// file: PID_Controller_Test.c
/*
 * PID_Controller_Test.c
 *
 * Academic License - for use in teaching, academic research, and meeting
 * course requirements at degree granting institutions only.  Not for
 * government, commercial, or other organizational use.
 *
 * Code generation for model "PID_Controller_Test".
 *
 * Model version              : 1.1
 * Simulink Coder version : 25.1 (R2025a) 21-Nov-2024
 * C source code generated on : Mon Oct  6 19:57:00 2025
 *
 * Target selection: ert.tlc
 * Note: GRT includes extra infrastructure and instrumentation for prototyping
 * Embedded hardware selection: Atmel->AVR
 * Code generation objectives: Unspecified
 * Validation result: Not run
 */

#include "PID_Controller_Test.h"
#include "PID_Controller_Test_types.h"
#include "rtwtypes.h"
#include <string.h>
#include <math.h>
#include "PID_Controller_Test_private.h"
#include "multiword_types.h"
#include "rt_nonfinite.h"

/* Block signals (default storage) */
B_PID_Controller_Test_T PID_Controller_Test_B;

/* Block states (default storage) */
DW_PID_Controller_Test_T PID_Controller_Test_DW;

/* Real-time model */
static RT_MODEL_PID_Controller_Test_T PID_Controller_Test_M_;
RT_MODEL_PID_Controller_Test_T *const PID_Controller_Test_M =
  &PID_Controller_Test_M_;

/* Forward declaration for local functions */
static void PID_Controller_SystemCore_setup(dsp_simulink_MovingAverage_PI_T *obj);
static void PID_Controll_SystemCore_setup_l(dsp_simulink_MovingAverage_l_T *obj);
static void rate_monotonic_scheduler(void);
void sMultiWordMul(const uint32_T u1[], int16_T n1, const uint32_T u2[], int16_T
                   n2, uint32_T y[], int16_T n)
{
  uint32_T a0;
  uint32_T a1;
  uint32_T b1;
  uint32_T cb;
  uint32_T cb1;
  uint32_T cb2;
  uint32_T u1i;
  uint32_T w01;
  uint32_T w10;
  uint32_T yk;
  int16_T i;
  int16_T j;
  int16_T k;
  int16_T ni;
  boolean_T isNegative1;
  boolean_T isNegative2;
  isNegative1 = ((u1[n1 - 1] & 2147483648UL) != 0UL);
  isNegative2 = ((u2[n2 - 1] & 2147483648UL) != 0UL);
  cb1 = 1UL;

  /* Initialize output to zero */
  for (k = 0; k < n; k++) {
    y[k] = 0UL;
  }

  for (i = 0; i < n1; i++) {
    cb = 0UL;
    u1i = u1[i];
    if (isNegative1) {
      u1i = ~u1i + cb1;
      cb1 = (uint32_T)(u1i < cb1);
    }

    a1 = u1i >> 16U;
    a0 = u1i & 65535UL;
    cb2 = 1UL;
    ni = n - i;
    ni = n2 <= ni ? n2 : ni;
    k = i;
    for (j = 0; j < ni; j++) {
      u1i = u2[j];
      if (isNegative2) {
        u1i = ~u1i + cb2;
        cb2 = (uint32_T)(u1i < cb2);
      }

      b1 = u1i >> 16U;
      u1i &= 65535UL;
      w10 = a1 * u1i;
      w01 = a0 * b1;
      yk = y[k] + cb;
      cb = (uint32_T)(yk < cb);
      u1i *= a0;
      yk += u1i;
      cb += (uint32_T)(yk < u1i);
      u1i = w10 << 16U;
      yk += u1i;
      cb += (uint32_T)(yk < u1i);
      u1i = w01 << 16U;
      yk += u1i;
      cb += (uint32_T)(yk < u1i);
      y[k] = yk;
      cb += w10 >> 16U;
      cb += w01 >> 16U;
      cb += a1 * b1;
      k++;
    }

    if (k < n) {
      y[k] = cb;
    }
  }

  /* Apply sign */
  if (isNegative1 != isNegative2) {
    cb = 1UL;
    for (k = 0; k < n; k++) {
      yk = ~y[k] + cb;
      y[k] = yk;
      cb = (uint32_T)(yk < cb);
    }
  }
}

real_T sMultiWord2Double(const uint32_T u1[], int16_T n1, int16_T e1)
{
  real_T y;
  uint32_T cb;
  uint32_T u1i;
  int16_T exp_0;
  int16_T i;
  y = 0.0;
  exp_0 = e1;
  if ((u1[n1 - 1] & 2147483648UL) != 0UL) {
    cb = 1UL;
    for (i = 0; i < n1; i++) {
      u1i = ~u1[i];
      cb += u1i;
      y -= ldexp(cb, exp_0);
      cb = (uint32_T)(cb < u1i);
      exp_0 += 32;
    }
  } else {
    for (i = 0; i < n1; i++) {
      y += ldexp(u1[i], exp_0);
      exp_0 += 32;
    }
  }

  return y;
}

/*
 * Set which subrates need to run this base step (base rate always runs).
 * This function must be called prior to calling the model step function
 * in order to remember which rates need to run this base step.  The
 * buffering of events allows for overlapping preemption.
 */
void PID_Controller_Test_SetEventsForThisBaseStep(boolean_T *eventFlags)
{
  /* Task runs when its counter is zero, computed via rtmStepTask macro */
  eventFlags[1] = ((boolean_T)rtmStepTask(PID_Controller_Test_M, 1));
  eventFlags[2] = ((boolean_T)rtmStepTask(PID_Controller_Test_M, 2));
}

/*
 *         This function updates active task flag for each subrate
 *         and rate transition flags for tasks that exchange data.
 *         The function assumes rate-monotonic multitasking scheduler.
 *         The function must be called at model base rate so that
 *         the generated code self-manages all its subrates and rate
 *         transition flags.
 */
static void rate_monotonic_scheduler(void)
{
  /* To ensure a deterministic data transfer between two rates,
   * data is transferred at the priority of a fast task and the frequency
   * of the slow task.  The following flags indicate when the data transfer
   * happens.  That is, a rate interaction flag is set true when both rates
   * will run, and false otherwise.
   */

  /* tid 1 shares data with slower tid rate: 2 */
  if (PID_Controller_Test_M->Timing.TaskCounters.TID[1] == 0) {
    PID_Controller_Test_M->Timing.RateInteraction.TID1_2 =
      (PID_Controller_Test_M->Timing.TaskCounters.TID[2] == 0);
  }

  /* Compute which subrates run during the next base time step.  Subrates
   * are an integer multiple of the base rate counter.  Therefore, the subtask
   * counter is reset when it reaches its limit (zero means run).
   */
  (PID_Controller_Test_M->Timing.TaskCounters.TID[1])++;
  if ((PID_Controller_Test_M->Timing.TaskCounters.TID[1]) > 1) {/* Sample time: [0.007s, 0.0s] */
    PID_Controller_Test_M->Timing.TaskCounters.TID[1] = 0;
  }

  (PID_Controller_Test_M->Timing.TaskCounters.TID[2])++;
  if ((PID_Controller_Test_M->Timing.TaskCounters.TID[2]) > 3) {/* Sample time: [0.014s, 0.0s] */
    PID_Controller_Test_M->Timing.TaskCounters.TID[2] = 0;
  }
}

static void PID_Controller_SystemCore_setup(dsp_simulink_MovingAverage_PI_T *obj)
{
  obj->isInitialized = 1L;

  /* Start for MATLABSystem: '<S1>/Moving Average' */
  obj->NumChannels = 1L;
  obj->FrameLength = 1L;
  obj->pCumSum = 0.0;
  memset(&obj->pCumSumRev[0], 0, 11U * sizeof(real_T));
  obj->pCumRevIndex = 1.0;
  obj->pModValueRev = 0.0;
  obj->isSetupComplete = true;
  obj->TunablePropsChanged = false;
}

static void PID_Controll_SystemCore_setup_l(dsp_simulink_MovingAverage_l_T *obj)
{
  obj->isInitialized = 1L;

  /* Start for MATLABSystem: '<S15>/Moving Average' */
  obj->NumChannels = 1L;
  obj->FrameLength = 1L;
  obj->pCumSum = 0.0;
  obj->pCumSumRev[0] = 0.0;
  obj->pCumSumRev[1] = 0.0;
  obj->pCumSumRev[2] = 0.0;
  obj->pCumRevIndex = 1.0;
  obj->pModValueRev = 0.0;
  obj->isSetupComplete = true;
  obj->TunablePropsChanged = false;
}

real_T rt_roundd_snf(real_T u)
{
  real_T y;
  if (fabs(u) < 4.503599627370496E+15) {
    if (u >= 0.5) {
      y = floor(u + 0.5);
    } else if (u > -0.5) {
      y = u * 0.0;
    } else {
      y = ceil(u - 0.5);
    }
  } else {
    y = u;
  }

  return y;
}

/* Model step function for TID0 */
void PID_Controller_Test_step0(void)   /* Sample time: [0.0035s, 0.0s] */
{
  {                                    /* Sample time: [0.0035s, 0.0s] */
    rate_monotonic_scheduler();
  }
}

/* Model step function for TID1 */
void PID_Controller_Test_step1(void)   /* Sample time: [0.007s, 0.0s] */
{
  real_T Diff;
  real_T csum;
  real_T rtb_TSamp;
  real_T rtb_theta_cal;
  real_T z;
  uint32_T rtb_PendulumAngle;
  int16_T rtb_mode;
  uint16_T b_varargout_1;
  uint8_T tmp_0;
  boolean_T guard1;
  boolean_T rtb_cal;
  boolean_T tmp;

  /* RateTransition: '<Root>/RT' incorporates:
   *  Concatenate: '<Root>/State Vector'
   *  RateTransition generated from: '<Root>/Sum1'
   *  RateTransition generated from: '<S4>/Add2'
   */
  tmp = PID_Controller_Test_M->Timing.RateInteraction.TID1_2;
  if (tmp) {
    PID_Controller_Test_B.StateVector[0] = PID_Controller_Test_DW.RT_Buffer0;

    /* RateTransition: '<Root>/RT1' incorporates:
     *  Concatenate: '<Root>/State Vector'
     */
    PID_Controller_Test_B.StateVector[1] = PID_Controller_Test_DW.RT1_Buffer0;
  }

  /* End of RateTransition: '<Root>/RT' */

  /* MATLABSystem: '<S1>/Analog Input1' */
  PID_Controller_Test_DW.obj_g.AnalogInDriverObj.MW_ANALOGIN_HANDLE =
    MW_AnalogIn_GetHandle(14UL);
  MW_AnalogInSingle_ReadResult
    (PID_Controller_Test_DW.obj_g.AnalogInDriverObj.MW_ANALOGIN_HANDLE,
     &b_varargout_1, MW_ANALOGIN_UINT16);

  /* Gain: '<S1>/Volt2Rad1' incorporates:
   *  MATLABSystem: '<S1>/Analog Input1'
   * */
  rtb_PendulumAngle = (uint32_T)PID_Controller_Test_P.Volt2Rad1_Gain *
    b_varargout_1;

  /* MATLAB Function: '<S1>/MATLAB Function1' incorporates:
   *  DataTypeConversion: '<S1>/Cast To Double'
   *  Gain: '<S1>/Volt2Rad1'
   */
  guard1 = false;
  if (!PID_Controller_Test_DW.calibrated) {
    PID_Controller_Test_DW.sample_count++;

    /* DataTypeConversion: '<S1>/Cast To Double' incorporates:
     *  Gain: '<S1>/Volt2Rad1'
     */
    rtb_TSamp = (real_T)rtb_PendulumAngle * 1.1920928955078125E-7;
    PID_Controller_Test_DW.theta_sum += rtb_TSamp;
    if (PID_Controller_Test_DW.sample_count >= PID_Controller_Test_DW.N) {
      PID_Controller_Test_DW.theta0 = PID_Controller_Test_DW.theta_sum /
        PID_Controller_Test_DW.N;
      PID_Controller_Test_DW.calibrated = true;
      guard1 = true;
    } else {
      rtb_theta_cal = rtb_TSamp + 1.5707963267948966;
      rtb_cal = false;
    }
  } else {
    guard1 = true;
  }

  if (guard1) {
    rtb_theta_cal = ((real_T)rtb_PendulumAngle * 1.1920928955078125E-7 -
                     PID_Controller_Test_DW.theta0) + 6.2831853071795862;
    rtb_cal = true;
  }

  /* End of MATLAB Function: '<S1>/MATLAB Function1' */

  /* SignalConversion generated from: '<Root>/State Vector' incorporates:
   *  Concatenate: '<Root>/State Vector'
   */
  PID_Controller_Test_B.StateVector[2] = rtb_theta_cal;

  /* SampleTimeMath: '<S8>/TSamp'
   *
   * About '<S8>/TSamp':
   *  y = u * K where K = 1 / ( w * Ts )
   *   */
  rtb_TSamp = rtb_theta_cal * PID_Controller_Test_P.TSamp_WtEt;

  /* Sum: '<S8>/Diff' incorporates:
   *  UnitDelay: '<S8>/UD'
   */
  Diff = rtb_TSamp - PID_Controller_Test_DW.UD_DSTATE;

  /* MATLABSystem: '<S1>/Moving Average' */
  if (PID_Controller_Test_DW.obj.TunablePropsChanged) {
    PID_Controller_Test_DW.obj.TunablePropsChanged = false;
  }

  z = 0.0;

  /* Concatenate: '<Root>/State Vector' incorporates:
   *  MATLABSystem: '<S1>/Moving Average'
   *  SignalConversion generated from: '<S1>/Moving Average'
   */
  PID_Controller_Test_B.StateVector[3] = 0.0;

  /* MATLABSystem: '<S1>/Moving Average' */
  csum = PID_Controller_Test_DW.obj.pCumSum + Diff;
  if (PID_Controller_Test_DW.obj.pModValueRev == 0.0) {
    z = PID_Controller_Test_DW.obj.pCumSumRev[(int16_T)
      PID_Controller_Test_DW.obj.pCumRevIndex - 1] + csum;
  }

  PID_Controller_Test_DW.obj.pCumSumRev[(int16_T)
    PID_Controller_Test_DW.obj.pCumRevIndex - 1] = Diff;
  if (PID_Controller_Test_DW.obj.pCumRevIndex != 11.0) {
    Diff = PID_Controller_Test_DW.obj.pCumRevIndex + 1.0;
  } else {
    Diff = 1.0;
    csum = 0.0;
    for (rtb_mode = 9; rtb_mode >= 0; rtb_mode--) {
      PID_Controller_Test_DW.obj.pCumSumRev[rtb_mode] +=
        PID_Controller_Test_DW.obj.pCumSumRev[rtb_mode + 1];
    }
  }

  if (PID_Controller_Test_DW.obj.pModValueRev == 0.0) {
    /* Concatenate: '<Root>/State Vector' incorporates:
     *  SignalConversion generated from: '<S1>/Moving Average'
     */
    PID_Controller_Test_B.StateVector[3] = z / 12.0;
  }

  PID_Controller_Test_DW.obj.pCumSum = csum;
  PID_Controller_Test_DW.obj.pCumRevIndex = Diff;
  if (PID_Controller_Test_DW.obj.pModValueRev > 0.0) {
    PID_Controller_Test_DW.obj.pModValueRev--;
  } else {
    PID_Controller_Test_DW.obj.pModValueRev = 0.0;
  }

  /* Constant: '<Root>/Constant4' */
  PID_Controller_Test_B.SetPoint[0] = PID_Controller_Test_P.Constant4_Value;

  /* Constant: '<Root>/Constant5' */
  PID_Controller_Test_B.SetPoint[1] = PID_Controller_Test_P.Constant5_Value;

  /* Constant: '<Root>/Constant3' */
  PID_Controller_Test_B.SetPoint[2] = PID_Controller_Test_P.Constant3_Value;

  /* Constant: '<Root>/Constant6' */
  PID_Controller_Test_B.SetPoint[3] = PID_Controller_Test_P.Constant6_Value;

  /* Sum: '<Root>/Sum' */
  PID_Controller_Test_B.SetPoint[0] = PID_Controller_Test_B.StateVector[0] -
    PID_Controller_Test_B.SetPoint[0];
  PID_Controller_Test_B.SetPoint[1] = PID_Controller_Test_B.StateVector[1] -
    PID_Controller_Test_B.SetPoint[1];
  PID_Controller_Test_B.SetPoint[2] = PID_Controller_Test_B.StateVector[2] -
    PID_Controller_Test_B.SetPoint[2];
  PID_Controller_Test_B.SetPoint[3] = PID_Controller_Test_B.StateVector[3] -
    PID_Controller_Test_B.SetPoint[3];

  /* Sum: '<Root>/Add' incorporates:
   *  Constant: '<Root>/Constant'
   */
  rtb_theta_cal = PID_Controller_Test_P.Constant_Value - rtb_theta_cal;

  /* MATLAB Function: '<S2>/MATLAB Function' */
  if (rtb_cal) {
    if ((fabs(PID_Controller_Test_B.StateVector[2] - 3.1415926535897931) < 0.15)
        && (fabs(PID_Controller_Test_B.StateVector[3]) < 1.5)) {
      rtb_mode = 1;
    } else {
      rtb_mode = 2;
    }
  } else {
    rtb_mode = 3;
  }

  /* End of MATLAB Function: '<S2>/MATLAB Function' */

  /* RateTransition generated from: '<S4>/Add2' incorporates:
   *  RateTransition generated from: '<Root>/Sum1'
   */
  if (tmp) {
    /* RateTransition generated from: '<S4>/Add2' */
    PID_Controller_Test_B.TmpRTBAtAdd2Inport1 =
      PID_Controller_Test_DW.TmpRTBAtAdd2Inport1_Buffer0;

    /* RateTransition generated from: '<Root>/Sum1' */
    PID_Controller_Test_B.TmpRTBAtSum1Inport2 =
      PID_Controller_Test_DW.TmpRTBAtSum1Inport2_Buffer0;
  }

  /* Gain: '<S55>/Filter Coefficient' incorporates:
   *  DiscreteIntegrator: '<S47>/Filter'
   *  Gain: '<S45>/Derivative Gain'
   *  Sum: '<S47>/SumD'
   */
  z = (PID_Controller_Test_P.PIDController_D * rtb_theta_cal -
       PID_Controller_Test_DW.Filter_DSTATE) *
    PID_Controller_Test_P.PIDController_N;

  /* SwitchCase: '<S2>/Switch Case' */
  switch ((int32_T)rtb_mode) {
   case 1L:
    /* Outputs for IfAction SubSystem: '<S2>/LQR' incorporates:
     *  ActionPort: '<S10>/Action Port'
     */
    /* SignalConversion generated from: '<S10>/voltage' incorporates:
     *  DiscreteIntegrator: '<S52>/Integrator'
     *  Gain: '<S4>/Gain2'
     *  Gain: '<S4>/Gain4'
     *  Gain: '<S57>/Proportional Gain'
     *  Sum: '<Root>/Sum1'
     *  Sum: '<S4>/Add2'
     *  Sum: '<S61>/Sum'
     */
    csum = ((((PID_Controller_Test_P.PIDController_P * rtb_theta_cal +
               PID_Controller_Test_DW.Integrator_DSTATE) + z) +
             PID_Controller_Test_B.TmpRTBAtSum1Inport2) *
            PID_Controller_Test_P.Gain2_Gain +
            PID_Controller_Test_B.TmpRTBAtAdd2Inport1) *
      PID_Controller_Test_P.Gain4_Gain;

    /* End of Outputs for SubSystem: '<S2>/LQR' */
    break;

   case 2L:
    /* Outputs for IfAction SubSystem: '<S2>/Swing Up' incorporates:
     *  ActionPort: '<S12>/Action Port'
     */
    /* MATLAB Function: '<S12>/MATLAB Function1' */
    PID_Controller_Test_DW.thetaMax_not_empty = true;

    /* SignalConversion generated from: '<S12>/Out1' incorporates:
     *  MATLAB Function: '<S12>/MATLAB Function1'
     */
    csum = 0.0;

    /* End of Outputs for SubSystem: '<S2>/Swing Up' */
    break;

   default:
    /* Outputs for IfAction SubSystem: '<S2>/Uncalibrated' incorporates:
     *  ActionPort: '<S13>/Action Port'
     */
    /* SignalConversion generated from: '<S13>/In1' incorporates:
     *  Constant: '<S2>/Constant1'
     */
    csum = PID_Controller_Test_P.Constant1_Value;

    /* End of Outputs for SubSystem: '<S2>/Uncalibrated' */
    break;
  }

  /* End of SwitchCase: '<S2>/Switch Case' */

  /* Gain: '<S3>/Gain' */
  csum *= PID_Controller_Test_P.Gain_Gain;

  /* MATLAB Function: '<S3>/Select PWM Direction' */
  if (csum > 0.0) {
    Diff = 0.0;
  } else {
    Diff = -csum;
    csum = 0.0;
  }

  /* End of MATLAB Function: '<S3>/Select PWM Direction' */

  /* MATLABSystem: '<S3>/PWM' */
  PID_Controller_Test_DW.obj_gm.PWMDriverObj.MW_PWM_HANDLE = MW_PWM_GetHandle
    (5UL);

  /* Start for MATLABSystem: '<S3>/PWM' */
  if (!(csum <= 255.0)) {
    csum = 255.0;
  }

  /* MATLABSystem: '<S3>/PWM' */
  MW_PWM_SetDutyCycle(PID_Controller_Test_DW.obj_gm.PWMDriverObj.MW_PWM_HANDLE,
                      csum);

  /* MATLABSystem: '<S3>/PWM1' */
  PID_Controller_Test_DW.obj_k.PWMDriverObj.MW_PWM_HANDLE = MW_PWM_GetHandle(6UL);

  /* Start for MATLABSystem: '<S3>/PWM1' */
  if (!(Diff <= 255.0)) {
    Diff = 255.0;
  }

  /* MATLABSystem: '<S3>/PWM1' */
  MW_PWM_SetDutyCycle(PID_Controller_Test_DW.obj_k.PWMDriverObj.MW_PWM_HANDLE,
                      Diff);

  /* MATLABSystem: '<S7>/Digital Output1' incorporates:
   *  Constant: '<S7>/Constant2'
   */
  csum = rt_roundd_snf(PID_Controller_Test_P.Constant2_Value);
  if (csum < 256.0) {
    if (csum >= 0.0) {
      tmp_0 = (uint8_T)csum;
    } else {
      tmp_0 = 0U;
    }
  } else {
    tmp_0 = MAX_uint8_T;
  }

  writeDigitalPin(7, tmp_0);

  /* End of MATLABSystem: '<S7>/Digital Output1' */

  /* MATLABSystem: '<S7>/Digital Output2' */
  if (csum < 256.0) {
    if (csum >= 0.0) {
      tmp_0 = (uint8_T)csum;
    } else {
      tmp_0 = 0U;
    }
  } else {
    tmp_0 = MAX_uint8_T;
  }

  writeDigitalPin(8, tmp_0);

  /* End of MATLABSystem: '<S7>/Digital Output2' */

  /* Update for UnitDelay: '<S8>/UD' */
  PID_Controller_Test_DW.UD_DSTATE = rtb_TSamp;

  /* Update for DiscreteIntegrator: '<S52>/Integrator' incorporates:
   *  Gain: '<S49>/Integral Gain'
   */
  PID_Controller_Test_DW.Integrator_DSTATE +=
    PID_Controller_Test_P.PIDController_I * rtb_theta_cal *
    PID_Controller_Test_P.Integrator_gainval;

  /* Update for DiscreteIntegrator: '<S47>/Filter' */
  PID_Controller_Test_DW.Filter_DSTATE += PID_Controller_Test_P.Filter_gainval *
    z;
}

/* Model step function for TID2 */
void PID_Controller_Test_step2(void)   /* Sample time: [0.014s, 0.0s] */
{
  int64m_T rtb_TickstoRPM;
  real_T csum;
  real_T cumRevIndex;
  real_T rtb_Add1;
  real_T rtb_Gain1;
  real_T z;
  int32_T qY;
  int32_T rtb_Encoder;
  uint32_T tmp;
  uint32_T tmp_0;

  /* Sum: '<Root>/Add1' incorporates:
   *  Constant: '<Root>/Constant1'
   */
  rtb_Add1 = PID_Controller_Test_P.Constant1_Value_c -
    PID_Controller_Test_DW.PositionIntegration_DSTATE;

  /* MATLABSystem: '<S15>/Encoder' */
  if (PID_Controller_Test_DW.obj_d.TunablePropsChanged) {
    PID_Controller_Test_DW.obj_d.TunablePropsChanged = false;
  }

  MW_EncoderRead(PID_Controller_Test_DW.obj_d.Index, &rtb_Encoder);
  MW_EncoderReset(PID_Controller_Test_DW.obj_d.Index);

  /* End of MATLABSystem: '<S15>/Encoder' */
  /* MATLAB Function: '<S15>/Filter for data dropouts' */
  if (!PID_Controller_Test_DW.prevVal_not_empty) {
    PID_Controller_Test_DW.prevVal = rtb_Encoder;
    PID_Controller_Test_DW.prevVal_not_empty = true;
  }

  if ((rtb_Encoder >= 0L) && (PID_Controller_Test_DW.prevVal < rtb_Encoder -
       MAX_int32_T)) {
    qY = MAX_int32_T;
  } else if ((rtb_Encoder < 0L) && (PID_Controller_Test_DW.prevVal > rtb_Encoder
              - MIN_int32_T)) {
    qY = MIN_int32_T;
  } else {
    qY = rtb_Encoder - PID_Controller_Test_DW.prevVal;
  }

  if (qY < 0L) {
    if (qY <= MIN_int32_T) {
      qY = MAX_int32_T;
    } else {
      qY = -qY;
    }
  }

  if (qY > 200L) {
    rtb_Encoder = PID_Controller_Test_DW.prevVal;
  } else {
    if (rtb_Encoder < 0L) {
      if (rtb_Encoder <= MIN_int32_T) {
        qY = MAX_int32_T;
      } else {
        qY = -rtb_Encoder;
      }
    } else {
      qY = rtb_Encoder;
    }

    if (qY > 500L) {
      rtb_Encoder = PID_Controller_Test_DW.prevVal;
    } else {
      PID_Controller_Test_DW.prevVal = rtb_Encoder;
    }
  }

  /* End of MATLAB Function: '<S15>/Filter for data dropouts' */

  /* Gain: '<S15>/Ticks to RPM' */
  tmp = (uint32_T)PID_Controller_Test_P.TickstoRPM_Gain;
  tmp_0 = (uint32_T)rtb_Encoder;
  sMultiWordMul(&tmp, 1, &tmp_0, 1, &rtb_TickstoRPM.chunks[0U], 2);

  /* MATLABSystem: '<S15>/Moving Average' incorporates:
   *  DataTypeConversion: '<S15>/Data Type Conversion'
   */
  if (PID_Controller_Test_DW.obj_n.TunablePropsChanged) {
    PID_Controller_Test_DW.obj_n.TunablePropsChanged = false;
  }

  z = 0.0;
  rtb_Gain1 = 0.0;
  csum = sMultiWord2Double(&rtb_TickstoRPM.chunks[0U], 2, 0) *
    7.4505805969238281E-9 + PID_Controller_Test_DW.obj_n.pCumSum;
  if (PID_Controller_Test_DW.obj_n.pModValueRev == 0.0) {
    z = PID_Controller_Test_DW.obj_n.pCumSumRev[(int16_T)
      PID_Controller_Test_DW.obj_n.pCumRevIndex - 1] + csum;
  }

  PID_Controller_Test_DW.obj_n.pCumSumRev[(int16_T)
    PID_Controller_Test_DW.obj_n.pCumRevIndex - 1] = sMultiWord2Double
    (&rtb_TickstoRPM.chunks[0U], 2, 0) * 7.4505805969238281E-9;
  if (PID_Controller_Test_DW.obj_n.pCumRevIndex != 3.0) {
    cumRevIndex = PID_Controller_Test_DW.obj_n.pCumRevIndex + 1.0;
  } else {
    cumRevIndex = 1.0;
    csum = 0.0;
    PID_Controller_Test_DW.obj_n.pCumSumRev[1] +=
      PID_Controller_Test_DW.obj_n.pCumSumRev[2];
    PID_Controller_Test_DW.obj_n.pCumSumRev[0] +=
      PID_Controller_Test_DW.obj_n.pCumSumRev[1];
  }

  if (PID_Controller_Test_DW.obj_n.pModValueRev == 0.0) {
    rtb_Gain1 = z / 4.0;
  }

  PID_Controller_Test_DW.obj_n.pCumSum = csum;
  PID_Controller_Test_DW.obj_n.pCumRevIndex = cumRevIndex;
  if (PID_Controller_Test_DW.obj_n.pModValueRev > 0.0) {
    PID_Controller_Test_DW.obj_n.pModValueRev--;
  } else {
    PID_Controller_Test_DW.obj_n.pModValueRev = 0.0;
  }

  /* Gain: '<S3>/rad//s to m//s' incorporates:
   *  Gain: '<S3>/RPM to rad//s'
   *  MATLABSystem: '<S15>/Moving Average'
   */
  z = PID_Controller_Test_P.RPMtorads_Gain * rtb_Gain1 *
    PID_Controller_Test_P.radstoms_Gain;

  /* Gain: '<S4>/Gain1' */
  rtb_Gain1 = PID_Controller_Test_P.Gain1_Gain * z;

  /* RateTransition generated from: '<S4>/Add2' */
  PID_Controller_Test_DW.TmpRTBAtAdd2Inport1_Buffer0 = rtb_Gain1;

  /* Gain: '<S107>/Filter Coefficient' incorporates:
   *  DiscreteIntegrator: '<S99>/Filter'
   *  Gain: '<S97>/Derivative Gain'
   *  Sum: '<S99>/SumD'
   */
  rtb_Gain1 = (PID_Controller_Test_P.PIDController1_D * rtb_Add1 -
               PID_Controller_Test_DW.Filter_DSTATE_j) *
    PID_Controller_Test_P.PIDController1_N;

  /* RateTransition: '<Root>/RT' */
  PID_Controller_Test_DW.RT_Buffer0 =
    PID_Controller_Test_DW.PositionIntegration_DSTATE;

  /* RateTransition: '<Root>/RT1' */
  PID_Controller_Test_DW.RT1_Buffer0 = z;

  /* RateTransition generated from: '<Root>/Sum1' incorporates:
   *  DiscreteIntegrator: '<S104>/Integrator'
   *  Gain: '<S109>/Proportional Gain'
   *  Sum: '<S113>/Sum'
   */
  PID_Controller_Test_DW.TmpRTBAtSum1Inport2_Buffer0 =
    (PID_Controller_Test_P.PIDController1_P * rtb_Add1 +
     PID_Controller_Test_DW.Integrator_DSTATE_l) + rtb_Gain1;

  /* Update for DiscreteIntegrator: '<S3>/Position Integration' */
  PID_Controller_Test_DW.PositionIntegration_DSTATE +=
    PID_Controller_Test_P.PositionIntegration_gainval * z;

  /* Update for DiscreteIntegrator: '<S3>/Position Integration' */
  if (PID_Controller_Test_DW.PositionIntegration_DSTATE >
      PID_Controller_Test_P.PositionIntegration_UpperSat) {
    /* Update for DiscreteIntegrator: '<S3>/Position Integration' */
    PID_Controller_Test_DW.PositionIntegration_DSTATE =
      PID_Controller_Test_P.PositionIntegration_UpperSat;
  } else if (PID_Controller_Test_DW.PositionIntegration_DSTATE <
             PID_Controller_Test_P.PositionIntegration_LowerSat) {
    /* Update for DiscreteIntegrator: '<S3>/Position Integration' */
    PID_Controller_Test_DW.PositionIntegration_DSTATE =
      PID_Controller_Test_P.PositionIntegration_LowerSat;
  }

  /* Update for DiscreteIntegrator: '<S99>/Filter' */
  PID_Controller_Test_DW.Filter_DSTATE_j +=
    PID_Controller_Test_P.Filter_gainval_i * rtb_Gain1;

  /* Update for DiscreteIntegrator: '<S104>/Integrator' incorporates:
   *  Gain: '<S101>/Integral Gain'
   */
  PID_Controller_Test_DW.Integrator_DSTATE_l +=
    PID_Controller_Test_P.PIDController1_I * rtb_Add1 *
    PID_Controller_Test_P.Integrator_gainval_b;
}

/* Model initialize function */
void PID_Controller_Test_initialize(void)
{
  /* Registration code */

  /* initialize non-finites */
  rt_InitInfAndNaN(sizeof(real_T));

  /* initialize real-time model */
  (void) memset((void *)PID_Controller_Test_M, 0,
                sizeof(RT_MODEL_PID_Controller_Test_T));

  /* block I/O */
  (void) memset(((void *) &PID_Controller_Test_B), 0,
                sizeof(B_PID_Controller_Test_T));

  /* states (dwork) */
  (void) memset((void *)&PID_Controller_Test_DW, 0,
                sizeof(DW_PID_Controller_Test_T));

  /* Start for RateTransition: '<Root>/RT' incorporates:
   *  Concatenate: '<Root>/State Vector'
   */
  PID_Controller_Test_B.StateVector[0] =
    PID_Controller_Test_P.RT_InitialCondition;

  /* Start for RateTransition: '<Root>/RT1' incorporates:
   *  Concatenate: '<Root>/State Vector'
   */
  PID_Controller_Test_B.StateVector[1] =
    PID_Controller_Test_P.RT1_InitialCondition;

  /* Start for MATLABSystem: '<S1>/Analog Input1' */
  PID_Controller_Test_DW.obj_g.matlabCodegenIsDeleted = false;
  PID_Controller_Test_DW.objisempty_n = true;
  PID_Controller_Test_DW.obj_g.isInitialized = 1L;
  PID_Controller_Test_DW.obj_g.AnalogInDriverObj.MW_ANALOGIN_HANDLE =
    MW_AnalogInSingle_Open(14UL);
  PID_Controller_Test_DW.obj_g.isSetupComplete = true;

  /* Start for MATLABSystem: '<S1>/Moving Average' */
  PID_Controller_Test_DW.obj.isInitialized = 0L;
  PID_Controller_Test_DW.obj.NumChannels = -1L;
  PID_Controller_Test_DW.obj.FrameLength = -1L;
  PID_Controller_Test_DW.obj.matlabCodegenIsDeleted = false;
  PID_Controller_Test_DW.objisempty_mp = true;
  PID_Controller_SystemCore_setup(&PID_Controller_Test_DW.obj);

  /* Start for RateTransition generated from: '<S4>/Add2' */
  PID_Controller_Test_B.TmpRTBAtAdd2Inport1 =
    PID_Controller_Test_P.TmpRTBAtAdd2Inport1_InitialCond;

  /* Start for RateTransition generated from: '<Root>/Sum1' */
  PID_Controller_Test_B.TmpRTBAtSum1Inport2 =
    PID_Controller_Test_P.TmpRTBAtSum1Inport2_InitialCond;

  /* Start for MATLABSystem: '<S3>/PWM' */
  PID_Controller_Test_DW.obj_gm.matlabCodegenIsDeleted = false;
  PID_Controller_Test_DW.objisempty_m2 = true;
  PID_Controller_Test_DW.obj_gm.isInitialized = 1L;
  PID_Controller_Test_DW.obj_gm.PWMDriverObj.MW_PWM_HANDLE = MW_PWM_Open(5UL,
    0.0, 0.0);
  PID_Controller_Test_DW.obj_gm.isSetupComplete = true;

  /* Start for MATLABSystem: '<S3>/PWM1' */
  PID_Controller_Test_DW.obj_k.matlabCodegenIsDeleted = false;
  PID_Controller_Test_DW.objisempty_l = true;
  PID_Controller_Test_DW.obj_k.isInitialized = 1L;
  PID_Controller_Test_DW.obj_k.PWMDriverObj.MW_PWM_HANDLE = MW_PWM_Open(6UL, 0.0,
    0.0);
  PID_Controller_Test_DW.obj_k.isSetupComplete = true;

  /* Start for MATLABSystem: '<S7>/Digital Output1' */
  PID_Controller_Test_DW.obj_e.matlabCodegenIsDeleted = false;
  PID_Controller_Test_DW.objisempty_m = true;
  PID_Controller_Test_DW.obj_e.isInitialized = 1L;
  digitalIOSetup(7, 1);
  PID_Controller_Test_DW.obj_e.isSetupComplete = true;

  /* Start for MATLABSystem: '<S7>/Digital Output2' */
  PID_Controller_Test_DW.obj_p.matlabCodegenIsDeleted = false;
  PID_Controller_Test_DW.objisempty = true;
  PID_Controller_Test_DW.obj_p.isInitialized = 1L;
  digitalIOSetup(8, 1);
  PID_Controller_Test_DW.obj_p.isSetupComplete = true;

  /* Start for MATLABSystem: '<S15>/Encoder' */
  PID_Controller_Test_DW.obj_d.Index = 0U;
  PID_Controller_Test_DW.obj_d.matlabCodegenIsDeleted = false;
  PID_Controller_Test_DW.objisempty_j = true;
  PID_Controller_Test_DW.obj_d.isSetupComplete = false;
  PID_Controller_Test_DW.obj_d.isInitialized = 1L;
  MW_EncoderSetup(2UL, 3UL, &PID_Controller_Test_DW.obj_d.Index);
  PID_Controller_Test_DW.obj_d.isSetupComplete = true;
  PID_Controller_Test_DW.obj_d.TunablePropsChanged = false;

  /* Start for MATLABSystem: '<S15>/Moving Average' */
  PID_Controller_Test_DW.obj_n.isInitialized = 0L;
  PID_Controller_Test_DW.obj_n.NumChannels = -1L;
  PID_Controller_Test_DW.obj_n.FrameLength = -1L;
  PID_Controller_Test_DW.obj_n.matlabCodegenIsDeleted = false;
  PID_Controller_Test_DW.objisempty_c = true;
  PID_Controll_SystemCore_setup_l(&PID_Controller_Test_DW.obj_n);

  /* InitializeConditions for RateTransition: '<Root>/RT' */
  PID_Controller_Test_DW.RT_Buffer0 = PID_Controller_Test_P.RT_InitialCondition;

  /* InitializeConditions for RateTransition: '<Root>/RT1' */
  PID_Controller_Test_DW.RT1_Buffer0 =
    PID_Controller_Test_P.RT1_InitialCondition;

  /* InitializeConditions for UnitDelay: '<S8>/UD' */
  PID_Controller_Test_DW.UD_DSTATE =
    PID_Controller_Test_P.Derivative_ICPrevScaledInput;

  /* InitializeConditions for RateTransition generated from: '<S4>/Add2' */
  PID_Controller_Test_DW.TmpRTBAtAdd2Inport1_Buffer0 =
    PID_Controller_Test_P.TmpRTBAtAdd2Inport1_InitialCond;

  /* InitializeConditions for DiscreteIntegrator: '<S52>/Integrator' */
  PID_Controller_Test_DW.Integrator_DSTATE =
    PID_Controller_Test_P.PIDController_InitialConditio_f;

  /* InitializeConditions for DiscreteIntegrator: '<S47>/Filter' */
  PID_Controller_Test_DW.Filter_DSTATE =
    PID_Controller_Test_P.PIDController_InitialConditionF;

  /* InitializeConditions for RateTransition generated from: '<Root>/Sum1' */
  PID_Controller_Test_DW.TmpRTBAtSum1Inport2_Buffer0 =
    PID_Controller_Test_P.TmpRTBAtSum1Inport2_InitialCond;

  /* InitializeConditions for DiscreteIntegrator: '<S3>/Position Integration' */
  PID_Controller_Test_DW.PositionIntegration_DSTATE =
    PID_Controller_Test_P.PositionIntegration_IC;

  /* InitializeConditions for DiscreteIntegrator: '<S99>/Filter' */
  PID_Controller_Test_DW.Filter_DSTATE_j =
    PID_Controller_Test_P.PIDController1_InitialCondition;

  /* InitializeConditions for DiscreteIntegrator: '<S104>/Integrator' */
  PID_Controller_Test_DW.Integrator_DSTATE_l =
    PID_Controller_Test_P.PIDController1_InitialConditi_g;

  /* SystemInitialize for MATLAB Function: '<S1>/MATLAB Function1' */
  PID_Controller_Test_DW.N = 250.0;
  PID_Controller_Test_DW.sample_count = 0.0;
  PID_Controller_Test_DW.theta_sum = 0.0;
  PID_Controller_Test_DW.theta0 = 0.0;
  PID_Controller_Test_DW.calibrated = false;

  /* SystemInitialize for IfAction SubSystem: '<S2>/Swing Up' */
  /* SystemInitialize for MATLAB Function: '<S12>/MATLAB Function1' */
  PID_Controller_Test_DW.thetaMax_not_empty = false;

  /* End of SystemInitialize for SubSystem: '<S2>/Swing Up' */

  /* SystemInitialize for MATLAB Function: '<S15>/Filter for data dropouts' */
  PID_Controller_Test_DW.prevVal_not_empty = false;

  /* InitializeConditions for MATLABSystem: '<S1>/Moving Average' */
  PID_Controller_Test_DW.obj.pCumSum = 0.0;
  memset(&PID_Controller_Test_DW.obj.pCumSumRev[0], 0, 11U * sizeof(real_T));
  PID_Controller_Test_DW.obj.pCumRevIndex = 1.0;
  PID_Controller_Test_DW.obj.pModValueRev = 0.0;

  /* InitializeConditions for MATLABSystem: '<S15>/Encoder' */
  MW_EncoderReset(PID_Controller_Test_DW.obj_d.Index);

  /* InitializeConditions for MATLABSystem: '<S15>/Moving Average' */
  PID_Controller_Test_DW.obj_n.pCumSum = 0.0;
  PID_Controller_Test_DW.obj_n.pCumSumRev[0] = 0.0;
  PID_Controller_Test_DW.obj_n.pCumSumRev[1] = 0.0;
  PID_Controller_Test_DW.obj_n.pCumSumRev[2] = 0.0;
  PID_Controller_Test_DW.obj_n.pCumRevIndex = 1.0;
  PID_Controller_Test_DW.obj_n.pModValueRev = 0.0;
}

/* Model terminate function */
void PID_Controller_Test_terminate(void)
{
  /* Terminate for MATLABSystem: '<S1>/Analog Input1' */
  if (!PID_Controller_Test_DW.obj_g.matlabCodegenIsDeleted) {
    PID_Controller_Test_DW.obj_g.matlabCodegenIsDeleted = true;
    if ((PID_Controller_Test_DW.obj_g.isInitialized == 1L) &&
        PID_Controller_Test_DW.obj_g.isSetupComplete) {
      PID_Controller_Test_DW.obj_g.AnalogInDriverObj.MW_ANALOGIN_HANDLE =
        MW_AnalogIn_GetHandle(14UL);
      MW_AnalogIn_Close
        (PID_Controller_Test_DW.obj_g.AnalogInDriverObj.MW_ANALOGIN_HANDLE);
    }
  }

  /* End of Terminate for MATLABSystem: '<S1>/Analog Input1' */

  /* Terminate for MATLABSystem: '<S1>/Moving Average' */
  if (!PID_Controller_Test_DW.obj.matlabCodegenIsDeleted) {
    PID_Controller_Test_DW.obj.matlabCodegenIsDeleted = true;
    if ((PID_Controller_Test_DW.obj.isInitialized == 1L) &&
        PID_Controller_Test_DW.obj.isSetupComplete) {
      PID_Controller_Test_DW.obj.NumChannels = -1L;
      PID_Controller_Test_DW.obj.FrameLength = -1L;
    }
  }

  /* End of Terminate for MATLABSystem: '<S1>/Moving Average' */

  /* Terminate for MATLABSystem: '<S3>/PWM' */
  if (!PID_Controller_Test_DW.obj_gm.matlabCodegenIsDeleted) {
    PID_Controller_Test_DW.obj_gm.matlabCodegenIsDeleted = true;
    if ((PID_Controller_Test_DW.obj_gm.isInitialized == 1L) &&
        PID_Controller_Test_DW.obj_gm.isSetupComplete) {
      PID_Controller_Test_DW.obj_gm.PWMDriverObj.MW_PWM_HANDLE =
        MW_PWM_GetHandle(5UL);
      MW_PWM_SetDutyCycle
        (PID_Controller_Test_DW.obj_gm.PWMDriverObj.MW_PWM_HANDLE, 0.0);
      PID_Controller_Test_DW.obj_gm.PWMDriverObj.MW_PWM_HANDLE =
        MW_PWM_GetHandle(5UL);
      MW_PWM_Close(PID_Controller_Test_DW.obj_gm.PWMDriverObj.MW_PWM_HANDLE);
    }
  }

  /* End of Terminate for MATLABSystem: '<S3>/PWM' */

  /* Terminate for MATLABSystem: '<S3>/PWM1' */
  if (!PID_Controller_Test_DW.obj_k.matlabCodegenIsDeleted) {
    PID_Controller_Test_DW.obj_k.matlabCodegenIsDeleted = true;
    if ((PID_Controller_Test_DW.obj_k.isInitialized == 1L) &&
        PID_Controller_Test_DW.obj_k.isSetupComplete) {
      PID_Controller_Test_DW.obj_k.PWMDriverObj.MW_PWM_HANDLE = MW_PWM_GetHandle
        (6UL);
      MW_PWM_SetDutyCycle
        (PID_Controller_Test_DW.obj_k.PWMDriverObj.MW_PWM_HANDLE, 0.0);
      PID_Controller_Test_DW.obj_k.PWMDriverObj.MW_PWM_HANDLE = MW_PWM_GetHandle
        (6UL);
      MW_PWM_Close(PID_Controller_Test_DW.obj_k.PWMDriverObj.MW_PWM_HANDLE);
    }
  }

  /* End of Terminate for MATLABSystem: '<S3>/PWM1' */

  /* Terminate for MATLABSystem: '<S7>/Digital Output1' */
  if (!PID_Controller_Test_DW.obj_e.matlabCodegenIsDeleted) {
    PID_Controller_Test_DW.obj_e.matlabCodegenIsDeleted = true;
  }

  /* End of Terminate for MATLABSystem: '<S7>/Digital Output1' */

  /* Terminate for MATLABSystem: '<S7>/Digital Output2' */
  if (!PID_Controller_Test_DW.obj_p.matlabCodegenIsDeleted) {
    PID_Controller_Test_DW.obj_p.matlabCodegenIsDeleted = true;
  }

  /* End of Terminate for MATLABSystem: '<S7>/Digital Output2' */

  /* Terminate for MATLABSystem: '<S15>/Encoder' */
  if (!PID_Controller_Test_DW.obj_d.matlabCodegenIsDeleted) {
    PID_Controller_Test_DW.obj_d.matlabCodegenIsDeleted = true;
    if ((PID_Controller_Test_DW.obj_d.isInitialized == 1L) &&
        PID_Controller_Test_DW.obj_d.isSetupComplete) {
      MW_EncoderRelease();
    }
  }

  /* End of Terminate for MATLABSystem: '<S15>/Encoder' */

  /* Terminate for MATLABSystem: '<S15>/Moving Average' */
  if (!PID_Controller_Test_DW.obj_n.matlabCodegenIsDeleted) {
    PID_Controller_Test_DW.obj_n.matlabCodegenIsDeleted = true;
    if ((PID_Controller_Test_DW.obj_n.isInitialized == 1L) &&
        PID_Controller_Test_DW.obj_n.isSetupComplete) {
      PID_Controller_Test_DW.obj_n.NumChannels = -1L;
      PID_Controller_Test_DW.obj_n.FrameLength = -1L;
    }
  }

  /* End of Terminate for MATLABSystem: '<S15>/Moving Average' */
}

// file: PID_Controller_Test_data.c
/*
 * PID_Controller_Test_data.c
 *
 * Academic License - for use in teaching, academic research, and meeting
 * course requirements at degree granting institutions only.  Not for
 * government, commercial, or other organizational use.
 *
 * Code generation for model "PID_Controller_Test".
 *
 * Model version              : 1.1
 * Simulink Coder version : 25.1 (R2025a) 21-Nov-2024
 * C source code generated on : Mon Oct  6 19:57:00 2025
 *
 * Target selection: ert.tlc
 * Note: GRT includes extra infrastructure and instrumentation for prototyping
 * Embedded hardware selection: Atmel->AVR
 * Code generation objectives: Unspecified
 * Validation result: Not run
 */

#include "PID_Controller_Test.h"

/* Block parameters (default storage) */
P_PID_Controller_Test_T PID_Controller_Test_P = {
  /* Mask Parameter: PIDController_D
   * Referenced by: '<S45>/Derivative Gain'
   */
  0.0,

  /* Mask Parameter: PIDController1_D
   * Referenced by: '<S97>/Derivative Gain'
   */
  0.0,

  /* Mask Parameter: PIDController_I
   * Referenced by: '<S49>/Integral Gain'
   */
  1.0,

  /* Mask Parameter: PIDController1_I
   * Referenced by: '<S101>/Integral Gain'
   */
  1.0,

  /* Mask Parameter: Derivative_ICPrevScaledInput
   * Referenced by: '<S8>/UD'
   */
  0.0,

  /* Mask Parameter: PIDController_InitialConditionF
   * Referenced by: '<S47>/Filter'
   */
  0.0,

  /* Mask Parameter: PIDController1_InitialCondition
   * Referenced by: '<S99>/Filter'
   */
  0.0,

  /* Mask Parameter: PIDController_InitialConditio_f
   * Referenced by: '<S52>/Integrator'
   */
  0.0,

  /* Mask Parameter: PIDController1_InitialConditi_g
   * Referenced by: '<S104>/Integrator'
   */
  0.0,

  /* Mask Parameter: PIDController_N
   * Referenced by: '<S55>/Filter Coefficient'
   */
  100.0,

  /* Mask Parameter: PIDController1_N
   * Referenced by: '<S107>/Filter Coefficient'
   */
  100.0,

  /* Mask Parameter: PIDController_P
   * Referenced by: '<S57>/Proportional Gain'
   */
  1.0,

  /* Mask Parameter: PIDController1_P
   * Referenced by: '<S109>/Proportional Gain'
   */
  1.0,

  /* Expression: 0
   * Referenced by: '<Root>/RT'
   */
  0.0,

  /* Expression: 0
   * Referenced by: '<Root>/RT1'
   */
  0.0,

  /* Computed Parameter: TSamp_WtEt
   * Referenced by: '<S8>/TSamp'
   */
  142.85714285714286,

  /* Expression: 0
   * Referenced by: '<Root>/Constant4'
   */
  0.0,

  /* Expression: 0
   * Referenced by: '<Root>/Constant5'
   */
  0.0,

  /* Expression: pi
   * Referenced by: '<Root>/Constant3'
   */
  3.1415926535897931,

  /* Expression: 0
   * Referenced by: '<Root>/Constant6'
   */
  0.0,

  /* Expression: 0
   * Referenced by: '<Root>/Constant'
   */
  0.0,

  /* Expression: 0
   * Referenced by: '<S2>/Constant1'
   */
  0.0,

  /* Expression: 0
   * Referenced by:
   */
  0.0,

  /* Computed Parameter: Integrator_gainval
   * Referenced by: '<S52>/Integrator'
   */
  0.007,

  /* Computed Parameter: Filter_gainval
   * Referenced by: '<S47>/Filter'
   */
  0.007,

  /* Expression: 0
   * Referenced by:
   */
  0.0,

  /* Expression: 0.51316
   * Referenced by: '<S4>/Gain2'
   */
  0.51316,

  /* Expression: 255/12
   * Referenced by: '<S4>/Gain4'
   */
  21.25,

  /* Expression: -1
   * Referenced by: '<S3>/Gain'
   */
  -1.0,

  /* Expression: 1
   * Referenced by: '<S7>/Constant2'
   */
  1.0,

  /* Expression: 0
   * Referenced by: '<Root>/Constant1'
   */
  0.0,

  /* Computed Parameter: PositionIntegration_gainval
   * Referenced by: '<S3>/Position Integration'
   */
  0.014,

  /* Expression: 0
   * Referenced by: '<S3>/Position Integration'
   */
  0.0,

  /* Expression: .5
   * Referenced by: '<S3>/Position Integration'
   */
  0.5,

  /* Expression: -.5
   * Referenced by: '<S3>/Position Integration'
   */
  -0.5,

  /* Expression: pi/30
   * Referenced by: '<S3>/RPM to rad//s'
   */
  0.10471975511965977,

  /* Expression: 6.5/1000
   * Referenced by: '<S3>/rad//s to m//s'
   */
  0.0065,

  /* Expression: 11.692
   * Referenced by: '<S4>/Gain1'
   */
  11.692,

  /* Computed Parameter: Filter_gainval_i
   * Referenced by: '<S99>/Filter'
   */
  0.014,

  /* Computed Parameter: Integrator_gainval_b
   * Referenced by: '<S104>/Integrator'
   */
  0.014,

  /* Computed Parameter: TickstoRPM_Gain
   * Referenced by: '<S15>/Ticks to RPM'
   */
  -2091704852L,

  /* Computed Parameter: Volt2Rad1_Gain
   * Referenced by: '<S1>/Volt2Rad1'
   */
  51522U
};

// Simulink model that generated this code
simulink model "PID_Controller_Test"  (R2025a)
settings: Solver=FixedStepAuto  StartTime=0.0  StopTime=Inf  FixedStep=0.0035  RelTol=1e-3  EnableMultiTasking=on
model workspace (MAT data in the model file):
  encoderDt = 0.014
undefined symbols (not defined in the file or in its folder): DiscIntNeverNeededParam
libraries: arduinolib x5, dspstat3 x2, slpidlib x2, simulink x1, arduinosensorlib x1

== system PID_Controller_Test ==
  Add : Sum  Inputs=+-
  Add1 : Sum  Inputs=+-
  Angle Measurement : Subsystem
  Constant{,1,4..6} (5 alike) : Constant  Value=0
  Constant3 : Constant  Value=pi
  Mode Selection : Subsystem
  Motor Controller : Subsystem
  Motor Dynamics Model : Subsystem
  PID Controller : slpidlib/PID Controller  Controller=PID  Form=Parallel  TimeDomain=Discrete-time  UseExternalTs=off  SampleTime=-1  IntegratorMethod=Forward Euler  FilterMethod=Forward Euler  ControllerParametersSource=internal  P=1  I=1  UseKiTs=off  D=0  UseExternalDerivativeSource=off  N=100  UseFilter=on  TunerSelectOption=Transfer Function Based (PID Tuner App)  InitialConditionSource=internal  InitialConditionForIntegrator=0  InitialConditionForFilter=0  DifferentiatorICPrevScaledInput=0  ExternalReset=none  TrackingMode=off  Kt=1  LimitOutput=off  SatLimitsSource=internal  UpperSaturationLimit=inf  LowerSaturationLimit=-inf  LinearizeAsGain=on  AntiWindupMode=none  Kb=1  LimitIntegrator=off  UpperIntegratorSaturationLimit=inf  LowerIntegratorSaturationLimit=-inf  POutMin=[]  POutMax=[]  IOutMin=[]  IOutMax=[]  DOutMin=[]  DOutMax=[]  NOutMin=[]  NOutMax=[]  SumOutMin=[]  SumOutMax=[]  SaturationOutMin=[]  SaturationOutMax=[]  PParamMin=[]  PParamMax=[]  IParamMin=[]  IParamMax=[]  DParamMin=[]  DParamMax=[]  NParamMin=[]  NParamMax=[]  KbParamMin=[]  KbParamMax=[]  KtParamMin=[]  KtParamMax=[]  KbOutMin=[]  KbOutMax=[]  KtOutMin=[]  KtOutMax=[]  IntegratorOutMin=[]  IntegratorOutMax=[]  FilterOutMin=[]  FilterOutMax=[]  SumI1OutMin=[]  SumI1OutMax=[]  SumI2OutMin=[]  SumI2OutMax=[]  SumI3OutMin=[]  SumI3OutMax=[]  SumI4OutMin=[]  SumI4OutMax=[]  SumDOutMin=[]  SumDOutMax=[]  DifferentiatorOutMin=[]  DifferentiatorOutMax=[]  FilterDiffOutCoefMin=[]  FilterDiffOutCoefMax=[]  ReciprocalOutMin=[]  ReciprocalOutMax=[]  SumDenOutMin=[]  SumDenOutMax=[]  SumNumOutMin=[]  SumNumOutMax=[]  DivideOutMin=[]  DivideOutMax=[]  UdiffTsProdOutMin=[]  UdiffTsProdOutMax=[]  NTsProdOutMin=[]  NTsProdOutMax=[]  UintegralTsProdOutMin=[]  UintegralTsProdOutMax=[]  UngainTsProdOutMin=[]  UngainTsProdOutMax=[]  ClampingZeroOutDataTypeStr=Inherit: Inherit via back propagation  ClampingZeroOutMin=[]  ClampingZeroOutMax=[]  FilterDenConstantOutDataTypeStr=Inherit: Inherit via back propagation  FilterDenConstantOutMin=[]  FilterDenConstantOutMax=[]  PCopyOutDataTypeStr=Inherit: Inherit via back propagation  PCopyOutMin=[]  PCopyOutMax=[]  NCopyOutDataTypeStr=Inherit: Inherit via back propagation  NCopyOutMin=[]  NCopyOutMax=[]  IntegratorContinuousStateAttributes=''  IntegratorStateMustResolveToSignalObject=off  IntegratorRTWStateStorageClass=Auto  FilterContinuousStateAttributes=''  FilterStateMustResolveToSignalObject=off  FilterRTWStateStorageClass=Auto  ParallelPVariant=InternalParameters  IdealPVariant=Disabled  IVariant=InternalParameters  DVariant=InternalParameters  IntegratorVariant=Discrete  SatVariant=Disabled  AWVariant=Passthrough  PCopyVariant=Disabled  TRVariant=Disabled  FdbkBlocksVariant=Forward  IdealPFdbkVariant=Disabled  SatFdbkVariant=Disabled  DerivativeFilterVariant=ForwardEulerFilter  NVariant=InternalParameters  NCopyVariant=Disabled  FilterICVariant=InternalICsFilter  IntegratorICVariant=InternalICs  ExternalResetVariant=Disabled  TRSumVariant=Passthrough  SumFdbkVariant=Disabled  SumVariant=Sum_PID  TsampFilterVariant=InternalTs  TsampNgainVariant=Passthrough  TsampIntegralVariant=Disabled_SignalSpec  ExternalSaturationOutDataTypeStr=Inherit: Same as second input  DerivativeSourceVariant=ErrorSignal  PreIntVariant=InternalPreInt
  PID Controller1 : slpidlib/PID Controller  Controller=PID  Form=Parallel  TimeDomain=Discrete-time  UseExternalTs=off  SampleTime=-1  IntegratorMethod=Forward Euler  FilterMethod=Forward Euler  ControllerParametersSource=internal  P=1  I=1  UseKiTs=off  D=0  UseExternalDerivativeSource=off  N=100  UseFilter=on  TunerSelectOption=Transfer Function Based (PID Tuner App)  InitialConditionSource=internal  InitialConditionForIntegrator=0  InitialConditionForFilter=0  DifferentiatorICPrevScaledInput=0  ExternalReset=none  TrackingMode=off  Kt=1  LimitOutput=off  SatLimitsSource=internal  UpperSaturationLimit=inf  LowerSaturationLimit=-inf  LinearizeAsGain=on  AntiWindupMode=none  Kb=1  LimitIntegrator=off  UpperIntegratorSaturationLimit=inf  LowerIntegratorSaturationLimit=-inf  POutMin=[]  POutMax=[]  IOutMin=[]  IOutMax=[]  DOutMin=[]  DOutMax=[]  NOutMin=[]  NOutMax=[]  SumOutMin=[]  SumOutMax=[]  SaturationOutMin=[]  SaturationOutMax=[]  PParamMin=[]  PParamMax=[]  IParamMin=[]  IParamMax=[]  DParamMin=[]  DParamMax=[]  NParamMin=[]  NParamMax=[]  KbParamMin=[]  KbParamMax=[]  KtParamMin=[]  KtParamMax=[]  KbOutMin=[]  KbOutMax=[]  KtOutMin=[]  KtOutMax=[]  IntegratorOutMin=[]  IntegratorOutMax=[]  FilterOutMin=[]  FilterOutMax=[]  SumI1OutMin=[]  SumI1OutMax=[]  SumI2OutMin=[]  SumI2OutMax=[]  SumI3OutMin=[]  SumI3OutMax=[]  SumI4OutMin=[]  SumI4OutMax=[]  SumDOutMin=[]  SumDOutMax=[]  DifferentiatorOutMin=[]  DifferentiatorOutMax=[]  FilterDiffOutCoefMin=[]  FilterDiffOutCoefMax=[]  ReciprocalOutMin=[]  ReciprocalOutMax=[]  SumDenOutMin=[]  SumDenOutMax=[]  SumNumOutMin=[]  SumNumOutMax=[]  DivideOutMin=[]  DivideOutMax=[]  UdiffTsProdOutMin=[]  UdiffTsProdOutMax=[]  NTsProdOutMin=[]  NTsProdOutMax=[]  UintegralTsProdOutMin=[]  UintegralTsProdOutMax=[]  UngainTsProdOutMin=[]  UngainTsProdOutMax=[]  ClampingZeroOutDataTypeStr=Inherit: Inherit via back propagation  ClampingZeroOutMin=[]  ClampingZeroOutMax=[]  FilterDenConstantOutDataTypeStr=Inherit: Inherit via back propagation  FilterDenConstantOutMin=[]  FilterDenConstantOutMax=[]  PCopyOutDataTypeStr=Inherit: Inherit via back propagation  PCopyOutMin=[]  PCopyOutMax=[]  NCopyOutDataTypeStr=Inherit: Inherit via back propagation  NCopyOutMin=[]  NCopyOutMax=[]  IntegratorContinuousStateAttributes=''  IntegratorStateMustResolveToSignalObject=off  IntegratorRTWStateStorageClass=Auto  FilterContinuousStateAttributes=''  FilterStateMustResolveToSignalObject=off  FilterRTWStateStorageClass=Auto  ParallelPVariant=InternalParameters  IdealPVariant=Disabled  IVariant=InternalParameters  DVariant=InternalParameters  IntegratorVariant=Discrete  SatVariant=Disabled  AWVariant=Passthrough  PCopyVariant=Disabled  TRVariant=Disabled  FdbkBlocksVariant=Forward  IdealPFdbkVariant=Disabled  SatFdbkVariant=Disabled  DerivativeFilterVariant=ForwardEulerFilter  NVariant=InternalParameters  NCopyVariant=Disabled  FilterICVariant=InternalICsFilter  IntegratorICVariant=InternalICs  ExternalResetVariant=Disabled  TRSumVariant=Passthrough  SumFdbkVariant=Disabled  SumVariant=Sum_PID  TsampFilterVariant=InternalTs  TsampNgainVariant=Passthrough  TsampIntegralVariant=Disabled_SignalSpec  ExternalSaturationOutDataTypeStr=Inherit: Same as second input  DerivativeSourceVariant=ErrorSignal  PreIntVariant=InternalPreInt
  Pin Setup : Subsystem
  RT : RateTransition
  RT1 : RateTransition  OutPortSampleTime=0.007
  Scope : Scope
  Set Point : Concatenate  NumInputs=4
  State Vector : Concatenate  NumInputs=4
  Sum : Sum  Inputs=|+-
  Sum1 : Sum  Inputs=|++
  wires:
  Motor Controller/1(Position) -> [pos], RT/1  "x"
  Constant4/1 -> Set Point/1
  Angle Measurement/2(Theta_dot (rad/s)) -> State Vector/4  "theta_dot"
  Angle Measurement/3(calibrated) -> [Cal]
  Constant3/1 -> Set Point/3
  Sum/1 -> Scope/1
  Mode Selection/1(u) -> Motor Controller/1(PWM Signal)
  State Vector/1 -> [X], Sum/1
  Motor Controller/2(Velocity) -> [Vel], RT1/1  "x_dot"
  [Cal] -> Mode Selection/3(calibrated)
  Constant5/1 -> Set Point/2
  [Vel] -> Motor Dynamics Model/1(Vel)
  RT1/1 -> State Vector/2
  Angle Measurement/1(Theta (rad)) -> [Theta], State Vector/3  "theta"
  Motor Dynamics Model/1(Voltage) -> Mode Selection/2(voltage)
  Set Point/1 -> Sum/2
  [X] -> Mode Selection/1(x)
  RT/1 -> State Vector/1
  Constant6/1 -> Set Point/4
  [Theta] -> Add/2
  Constant/1 -> Add/1
  Add/1 -> PID Controller/1
  Add1/1 -> PID Controller1/1
  Constant1/1 -> Add1/1
  [pos] -> Add1/2
  PID Controller/1 -> Sum1/1
  PID Controller1/1 -> Sum1/2
  Sum1/1 -> Motor Dynamics Model/2(Force)

== system PID_Controller_Test/Angle Measurement ==
  Analog Input1 : arduinolib/Analog Input  pinNumber=0  ReadResultsOnly=off  ConversionTriggerSource=Software  ExternalTriggerType=uint32( 0 )  OutputDataType=uint16  EnableConversionCompleteNotify=off  EnableOuputStatus=off  SampleTime=-1  blockPlatform=arduino
  Cast To Double : DataTypeConversion  OutDataTypeStr=double  SaturateOnIntegerOverflow=off  RndMeth=Floor
  Derivative : simulink/Discrete/Discrete Derivative  gainval=1.0  ICPrevScaledInput=0.0  OutMin=[]  OutMax=[]  OutDataType=fixdt(1, 16)  OutScaling=2^-10  RndMeth=Nearest  DoSatur=off
  MATLAB Function1 : MATLAB Function  TreatAsAtomicUnit=on
  Moving Average : dspstat3/Moving Average  Method=Sliding window  ForgettingFactorPort=off  SpecifyWindowLength=on  WindowLength=12  OverlapLength=11  AllowArbitraryInputLength=off  ForgettingFactor=0.9  SimulateUsing=Interpreted execution
  Volt2Rad1 : Gain  Gain=2*pi/1023
  Theta (rad) : Outport
  Theta_dot (rad/s) : Outport  Port=2
  calibrated : Outport  Port=3
  wires:
  Analog Input1/1 -> Volt2Rad1/1
  Volt2Rad1/1 -> Cast To Double/1  "Pendulum Angle"
  Cast To Double/1 -> MATLAB Function1/1(theta_raw)
  MATLAB Function1/1(theta_cal) -> Derivative/1, Theta (rad)/1
  Derivative/1 -> Moving Average/1
  Moving Average/1 -> Theta_dot (rad/s)/1
  MATLAB Function1/2(cal) -> calibrated/1

== system PID_Controller_Test/Mode Selection ==
  x : Inport
  voltage : Inport  Port=2
  calibrated : Inport  Port=3
  Constant1 : Constant  Value=0
  LQR : Subsystem  TreatAsAtomicUnit=on
  MATLAB Function : MATLAB Function  TreatAsAtomicUnit=on
  Merge : Merge  Inputs=3
  Swing Up : Subsystem  TreatAsAtomicUnit=on
  Switch Case : SwitchCase  CaseConditions={1,2}
  Uncalibrated : Subsystem  TreatAsAtomicUnit=on
  u : Outport
  wires:
  calibrated/1 -> MATLAB Function/2(calibrated)
  x/1 -> [X], MATLAB Function/1(x)
  MATLAB Function/1(mode) -> Switch Case/1
  Switch Case/1 -> LQR/Action
  LQR/1(Out1) -> Merge/1
  voltage/1 -> LQR/1(voltage)
  Switch Case/2 -> Swing Up/Action
  Swing Up/1(Out1) -> Merge/2
  Merge/1 -> u/1
  Switch Case/3 -> Uncalibrated/Action
  Constant1/1 -> Uncalibrated/1(In1)
  Uncalibrated/1(Out1) -> Merge/3
  [X] -> Swing Up/1(In1)

== system PID_Controller_Test/Motor Controller ==
  PWM Signal : Inport
  Gain : Gain  Gain=-1
  PWM : arduinolib/PWM  pinNumber=5  frequencyType=Default  desiredFrequency=490.2  achievableFrequency=490.2
  PWM1 : arduinolib/PWM  pinNumber=6  frequencyType=Default  desiredFrequency=490.2  achievableFrequency=490.2
  Position Integration : DiscreteIntegrator  SampleTime=encoderDt  LimitOutput=on  UpperSaturationLimit=.5  LowerSaturationLimit=-.5  ICPrevOutput=DiscIntNeverNeededParam  ICPrevScaledInput=DiscIntNeverNeededParam
  RPM Measurement : Subsystem
  RPM to rad/s : Gain  Gain=pi/30
  Select PWM Direction : MATLAB Function  TreatAsAtomicUnit=on
  rad/s to m/s : Gain  Gain=6.5/1000
  Position : Outport
  Velocity : Outport  Port=2
  wires:
  RPM to rad/s/1 -> rad/s to m/s/1
  Select PWM Direction/2(negPWM) -> PWM1/1
  RPM Measurement/1(RPM) -> RPM to rad/s/1  "Measured RPM"
  Position Integration/1 -> Position/1
  Select PWM Direction/1(PosPWM) -> PWM/1
  rad/s to m/s/1 -> Position Integration/1, Velocity/1
  PWM Signal/1 -> Gain/1
  Gain/1 -> Select PWM Direction/1(u)

== system PID_Controller_Test/Motor Dynamics Model ==
  Vel : Inport
  Force : Inport  Port=2
  Add2 : Sum
  Gain1 : Gain  Gain=11.692
  Gain2 : Gain  Gain=0.51316
  Gain4 : Gain  Gain=255/12
  Voltage : Outport
  wires:
  Gain2/1 -> Add2/2
  Force/1 -> Gain2/1
  Gain1/1 -> Add2/1
  Add2/1 -> Gain4/1
  Gain4/1 -> Voltage/1
  Vel/1 -> Gain1/1

== system PID_Controller_Test/Pin Setup ==
  Constant2 : Constant
  Digital Output1 : arduinolib/Digital Output  pinNumber=7  Direction=output  blockPlatform=arduino
  Digital Output2 : arduinolib/Digital Output  pinNumber=8  Direction=output  blockPlatform=arduino
  wires:
  Constant2/1 -> Digital Output1/1, Digital Output2/1

== system PID_Controller_Test/Mode Selection/LQR ==
  voltage : Inport
  Action Port : ActionPort  ActionPortLabel=case [ 1 ]:
  Out1 : Outport
  wires:
  voltage/1 -> Out1/1

== system PID_Controller_Test/Mode Selection/Swing Up ==
  In1 : Inport
  Action Port : ActionPort  ActionPortLabel=case [ 2 ]:
  MATLAB Function1 : MATLAB Function  TreatAsAtomicUnit=on
  Out1 : Outport
  wires:
  In1/1 -> MATLAB Function1/1(x)
  MATLAB Function1/1(u) -> Out1/1

== system PID_Controller_Test/Mode Selection/Uncalibrated ==
  In1 : Inport
  Action Port : ActionPort  ActionPortLabel=default:
  Out1 : Outport
  wires:
  In1/1 -> Out1/1

== system PID_Controller_Test/Motor Controller/RPM Measurement ==
  Data Type Conversion : DataTypeConversion  OutDataTypeStr=double  SaturateOnIntegerOverflow=off  RndMeth=Floor
  Display3 : Display
  Encoder : arduinosensorlib/Encoder  InputA=2  InputB=3  Mode=Reset at each Sample time  SampleTime=encoderDt
  Filter for data dropouts : MATLAB Function  TreatAsAtomicUnit=on
  Moving Average : dspstat3/Moving Average  Method=Sliding window  ForgettingFactorPort=off  SpecifyWindowLength=on  WindowLength=4  OverlapLength=3  AllowArbitraryInputLength=off  ForgettingFactor=0.9  SimulateUsing=Interpreted execution
  Scope : Scope
  Ticks to RPM : Gain  Gain=-1/(6.25*11*4)*60/encoderDt
  RPM : Outport
  wires:
  Filter for data dropouts/1(filtered) -> Ticks to RPM/1
  Encoder/1 -> Display3/1, Scope/1, Filter for data dropouts/1(currVal)
  Ticks to RPM/1 -> Data Type Conversion/1
  Data Type Conversion/1 -> Moving Average/1
  Moving Average/1 -> RPM/1

== matlab function PID_Controller_Test/Motor Controller/Select PWM Direction ==
function [PosPWM, negPWM] = PWMDir(u)
    if u > 0
        PosPWM = u;
        negPWM = 0;
    else
        negPWM = -u;
        PosPWM = 0;
    end
end

== matlab function PID_Controller_Test/Motor Controller/RPM Measurement/Filter for data dropouts ==
function filtered = filterEncoder(currVal)
%#codegen

persistent prevVal

% Initialize on first call
if isempty(prevVal)
    prevVal = currVal;
end

% Dropout detection
threshold = 200;  % Adjust based on your system

if abs(currVal - prevVal) > threshold
    % Bad reading: keep previous good value
    filtered = prevVal;
elseif abs(currVal) > 500
    % this is also a bad reading, nothing should be greater than this
    filtered = prevVal;
else
    % Good reading: update and pass through
    filtered = currVal;
    prevVal = currVal;
end

== matlab function PID_Controller_Test/Mode Selection/MATLAB Function ==
function mode = ControllerMode(x, calibrated)
% the controller mode selection acts on the state of the pendulum. In the
% standard stable configuration, the controller will center and perform a
% swing up. Once this is achieved, the controller moves into the LQR
% regulator for upright control.
%
% Inputs:
% x - full state vector [4x1]
% voltage - voltage control input [V]
% calibrated - calibration flag boolean

% demux the input state:

pos = x(1);
vel = x(2);
theta = x(3);
omega = x(4);

% if it's calibrated, continue
if calibrated
    % If it is close enough to the vertical position, run the LQR
    if abs(theta-pi) < 0.15 && abs(omega) < 1.5
        mode = 1;        
    else % if it is close enough to the downward position, run the swing up controller
        mode = 2;
    end
else
    mode = 3;
end

end

== matlab function PID_Controller_Test/Angle Measurement/MATLAB Function1 ==
function [theta_cal, cal] = calibrateAngle(theta_raw)
% Calibrates angle by averaging first N samples at startup,
% then subtracting the average offset and adding pi.
%
% Inputs:
%  - theta_raw : current raw angle measurement
%  - reset     : boolean flag to reset calibration (true at startup)
%
% Output:
%  - theta_cal : calibrated angle (aligned so initial avg = pi)

    persistent sample_count theta_sum theta0 calibrated N

    if isempty(calibrated)
        % Initialization on reset
        N = 250;                % number of samples to average
        sample_count = 0;
        theta_sum = 0;
        theta0 = 0;
        calibrated = false;
        cal = false;
    end

    if ~calibrated
        % Accumulate samples for averaging
        sample_count = sample_count + 1;
        theta_sum = theta_sum + theta_raw;
        
        if sample_count >= N
            theta0 = theta_sum / N;  % average offset
            calibrated = true;
            cal = true;
        end
    end

    if calibrated
        % After calibration, subtract offset and add pi
        theta_cal = theta_raw - theta0 + 2*pi;
        cal = true;
    else
        % During calibration phase, output raw angle
        theta_cal = theta_raw + 1/2*pi; 
        cal = false;
    end
end

== matlab function PID_Controller_Test/Mode Selection/Swing Up/MATLAB Function1 ==
function u = SwingUpController(x)

% demux the input state:
pos = x(1);
vel = x(2);
theta = x(3);
omega = x(4);

persistent thetaMax

if isempty(thetaMax)
    thetaMax = theta;
end

T = 1.1; % period of pendulum
t = 0.05; % acceleration time of pendulum

alphaBest = thetaMax * sin(2*pi/T*t);

u = 0;

end
